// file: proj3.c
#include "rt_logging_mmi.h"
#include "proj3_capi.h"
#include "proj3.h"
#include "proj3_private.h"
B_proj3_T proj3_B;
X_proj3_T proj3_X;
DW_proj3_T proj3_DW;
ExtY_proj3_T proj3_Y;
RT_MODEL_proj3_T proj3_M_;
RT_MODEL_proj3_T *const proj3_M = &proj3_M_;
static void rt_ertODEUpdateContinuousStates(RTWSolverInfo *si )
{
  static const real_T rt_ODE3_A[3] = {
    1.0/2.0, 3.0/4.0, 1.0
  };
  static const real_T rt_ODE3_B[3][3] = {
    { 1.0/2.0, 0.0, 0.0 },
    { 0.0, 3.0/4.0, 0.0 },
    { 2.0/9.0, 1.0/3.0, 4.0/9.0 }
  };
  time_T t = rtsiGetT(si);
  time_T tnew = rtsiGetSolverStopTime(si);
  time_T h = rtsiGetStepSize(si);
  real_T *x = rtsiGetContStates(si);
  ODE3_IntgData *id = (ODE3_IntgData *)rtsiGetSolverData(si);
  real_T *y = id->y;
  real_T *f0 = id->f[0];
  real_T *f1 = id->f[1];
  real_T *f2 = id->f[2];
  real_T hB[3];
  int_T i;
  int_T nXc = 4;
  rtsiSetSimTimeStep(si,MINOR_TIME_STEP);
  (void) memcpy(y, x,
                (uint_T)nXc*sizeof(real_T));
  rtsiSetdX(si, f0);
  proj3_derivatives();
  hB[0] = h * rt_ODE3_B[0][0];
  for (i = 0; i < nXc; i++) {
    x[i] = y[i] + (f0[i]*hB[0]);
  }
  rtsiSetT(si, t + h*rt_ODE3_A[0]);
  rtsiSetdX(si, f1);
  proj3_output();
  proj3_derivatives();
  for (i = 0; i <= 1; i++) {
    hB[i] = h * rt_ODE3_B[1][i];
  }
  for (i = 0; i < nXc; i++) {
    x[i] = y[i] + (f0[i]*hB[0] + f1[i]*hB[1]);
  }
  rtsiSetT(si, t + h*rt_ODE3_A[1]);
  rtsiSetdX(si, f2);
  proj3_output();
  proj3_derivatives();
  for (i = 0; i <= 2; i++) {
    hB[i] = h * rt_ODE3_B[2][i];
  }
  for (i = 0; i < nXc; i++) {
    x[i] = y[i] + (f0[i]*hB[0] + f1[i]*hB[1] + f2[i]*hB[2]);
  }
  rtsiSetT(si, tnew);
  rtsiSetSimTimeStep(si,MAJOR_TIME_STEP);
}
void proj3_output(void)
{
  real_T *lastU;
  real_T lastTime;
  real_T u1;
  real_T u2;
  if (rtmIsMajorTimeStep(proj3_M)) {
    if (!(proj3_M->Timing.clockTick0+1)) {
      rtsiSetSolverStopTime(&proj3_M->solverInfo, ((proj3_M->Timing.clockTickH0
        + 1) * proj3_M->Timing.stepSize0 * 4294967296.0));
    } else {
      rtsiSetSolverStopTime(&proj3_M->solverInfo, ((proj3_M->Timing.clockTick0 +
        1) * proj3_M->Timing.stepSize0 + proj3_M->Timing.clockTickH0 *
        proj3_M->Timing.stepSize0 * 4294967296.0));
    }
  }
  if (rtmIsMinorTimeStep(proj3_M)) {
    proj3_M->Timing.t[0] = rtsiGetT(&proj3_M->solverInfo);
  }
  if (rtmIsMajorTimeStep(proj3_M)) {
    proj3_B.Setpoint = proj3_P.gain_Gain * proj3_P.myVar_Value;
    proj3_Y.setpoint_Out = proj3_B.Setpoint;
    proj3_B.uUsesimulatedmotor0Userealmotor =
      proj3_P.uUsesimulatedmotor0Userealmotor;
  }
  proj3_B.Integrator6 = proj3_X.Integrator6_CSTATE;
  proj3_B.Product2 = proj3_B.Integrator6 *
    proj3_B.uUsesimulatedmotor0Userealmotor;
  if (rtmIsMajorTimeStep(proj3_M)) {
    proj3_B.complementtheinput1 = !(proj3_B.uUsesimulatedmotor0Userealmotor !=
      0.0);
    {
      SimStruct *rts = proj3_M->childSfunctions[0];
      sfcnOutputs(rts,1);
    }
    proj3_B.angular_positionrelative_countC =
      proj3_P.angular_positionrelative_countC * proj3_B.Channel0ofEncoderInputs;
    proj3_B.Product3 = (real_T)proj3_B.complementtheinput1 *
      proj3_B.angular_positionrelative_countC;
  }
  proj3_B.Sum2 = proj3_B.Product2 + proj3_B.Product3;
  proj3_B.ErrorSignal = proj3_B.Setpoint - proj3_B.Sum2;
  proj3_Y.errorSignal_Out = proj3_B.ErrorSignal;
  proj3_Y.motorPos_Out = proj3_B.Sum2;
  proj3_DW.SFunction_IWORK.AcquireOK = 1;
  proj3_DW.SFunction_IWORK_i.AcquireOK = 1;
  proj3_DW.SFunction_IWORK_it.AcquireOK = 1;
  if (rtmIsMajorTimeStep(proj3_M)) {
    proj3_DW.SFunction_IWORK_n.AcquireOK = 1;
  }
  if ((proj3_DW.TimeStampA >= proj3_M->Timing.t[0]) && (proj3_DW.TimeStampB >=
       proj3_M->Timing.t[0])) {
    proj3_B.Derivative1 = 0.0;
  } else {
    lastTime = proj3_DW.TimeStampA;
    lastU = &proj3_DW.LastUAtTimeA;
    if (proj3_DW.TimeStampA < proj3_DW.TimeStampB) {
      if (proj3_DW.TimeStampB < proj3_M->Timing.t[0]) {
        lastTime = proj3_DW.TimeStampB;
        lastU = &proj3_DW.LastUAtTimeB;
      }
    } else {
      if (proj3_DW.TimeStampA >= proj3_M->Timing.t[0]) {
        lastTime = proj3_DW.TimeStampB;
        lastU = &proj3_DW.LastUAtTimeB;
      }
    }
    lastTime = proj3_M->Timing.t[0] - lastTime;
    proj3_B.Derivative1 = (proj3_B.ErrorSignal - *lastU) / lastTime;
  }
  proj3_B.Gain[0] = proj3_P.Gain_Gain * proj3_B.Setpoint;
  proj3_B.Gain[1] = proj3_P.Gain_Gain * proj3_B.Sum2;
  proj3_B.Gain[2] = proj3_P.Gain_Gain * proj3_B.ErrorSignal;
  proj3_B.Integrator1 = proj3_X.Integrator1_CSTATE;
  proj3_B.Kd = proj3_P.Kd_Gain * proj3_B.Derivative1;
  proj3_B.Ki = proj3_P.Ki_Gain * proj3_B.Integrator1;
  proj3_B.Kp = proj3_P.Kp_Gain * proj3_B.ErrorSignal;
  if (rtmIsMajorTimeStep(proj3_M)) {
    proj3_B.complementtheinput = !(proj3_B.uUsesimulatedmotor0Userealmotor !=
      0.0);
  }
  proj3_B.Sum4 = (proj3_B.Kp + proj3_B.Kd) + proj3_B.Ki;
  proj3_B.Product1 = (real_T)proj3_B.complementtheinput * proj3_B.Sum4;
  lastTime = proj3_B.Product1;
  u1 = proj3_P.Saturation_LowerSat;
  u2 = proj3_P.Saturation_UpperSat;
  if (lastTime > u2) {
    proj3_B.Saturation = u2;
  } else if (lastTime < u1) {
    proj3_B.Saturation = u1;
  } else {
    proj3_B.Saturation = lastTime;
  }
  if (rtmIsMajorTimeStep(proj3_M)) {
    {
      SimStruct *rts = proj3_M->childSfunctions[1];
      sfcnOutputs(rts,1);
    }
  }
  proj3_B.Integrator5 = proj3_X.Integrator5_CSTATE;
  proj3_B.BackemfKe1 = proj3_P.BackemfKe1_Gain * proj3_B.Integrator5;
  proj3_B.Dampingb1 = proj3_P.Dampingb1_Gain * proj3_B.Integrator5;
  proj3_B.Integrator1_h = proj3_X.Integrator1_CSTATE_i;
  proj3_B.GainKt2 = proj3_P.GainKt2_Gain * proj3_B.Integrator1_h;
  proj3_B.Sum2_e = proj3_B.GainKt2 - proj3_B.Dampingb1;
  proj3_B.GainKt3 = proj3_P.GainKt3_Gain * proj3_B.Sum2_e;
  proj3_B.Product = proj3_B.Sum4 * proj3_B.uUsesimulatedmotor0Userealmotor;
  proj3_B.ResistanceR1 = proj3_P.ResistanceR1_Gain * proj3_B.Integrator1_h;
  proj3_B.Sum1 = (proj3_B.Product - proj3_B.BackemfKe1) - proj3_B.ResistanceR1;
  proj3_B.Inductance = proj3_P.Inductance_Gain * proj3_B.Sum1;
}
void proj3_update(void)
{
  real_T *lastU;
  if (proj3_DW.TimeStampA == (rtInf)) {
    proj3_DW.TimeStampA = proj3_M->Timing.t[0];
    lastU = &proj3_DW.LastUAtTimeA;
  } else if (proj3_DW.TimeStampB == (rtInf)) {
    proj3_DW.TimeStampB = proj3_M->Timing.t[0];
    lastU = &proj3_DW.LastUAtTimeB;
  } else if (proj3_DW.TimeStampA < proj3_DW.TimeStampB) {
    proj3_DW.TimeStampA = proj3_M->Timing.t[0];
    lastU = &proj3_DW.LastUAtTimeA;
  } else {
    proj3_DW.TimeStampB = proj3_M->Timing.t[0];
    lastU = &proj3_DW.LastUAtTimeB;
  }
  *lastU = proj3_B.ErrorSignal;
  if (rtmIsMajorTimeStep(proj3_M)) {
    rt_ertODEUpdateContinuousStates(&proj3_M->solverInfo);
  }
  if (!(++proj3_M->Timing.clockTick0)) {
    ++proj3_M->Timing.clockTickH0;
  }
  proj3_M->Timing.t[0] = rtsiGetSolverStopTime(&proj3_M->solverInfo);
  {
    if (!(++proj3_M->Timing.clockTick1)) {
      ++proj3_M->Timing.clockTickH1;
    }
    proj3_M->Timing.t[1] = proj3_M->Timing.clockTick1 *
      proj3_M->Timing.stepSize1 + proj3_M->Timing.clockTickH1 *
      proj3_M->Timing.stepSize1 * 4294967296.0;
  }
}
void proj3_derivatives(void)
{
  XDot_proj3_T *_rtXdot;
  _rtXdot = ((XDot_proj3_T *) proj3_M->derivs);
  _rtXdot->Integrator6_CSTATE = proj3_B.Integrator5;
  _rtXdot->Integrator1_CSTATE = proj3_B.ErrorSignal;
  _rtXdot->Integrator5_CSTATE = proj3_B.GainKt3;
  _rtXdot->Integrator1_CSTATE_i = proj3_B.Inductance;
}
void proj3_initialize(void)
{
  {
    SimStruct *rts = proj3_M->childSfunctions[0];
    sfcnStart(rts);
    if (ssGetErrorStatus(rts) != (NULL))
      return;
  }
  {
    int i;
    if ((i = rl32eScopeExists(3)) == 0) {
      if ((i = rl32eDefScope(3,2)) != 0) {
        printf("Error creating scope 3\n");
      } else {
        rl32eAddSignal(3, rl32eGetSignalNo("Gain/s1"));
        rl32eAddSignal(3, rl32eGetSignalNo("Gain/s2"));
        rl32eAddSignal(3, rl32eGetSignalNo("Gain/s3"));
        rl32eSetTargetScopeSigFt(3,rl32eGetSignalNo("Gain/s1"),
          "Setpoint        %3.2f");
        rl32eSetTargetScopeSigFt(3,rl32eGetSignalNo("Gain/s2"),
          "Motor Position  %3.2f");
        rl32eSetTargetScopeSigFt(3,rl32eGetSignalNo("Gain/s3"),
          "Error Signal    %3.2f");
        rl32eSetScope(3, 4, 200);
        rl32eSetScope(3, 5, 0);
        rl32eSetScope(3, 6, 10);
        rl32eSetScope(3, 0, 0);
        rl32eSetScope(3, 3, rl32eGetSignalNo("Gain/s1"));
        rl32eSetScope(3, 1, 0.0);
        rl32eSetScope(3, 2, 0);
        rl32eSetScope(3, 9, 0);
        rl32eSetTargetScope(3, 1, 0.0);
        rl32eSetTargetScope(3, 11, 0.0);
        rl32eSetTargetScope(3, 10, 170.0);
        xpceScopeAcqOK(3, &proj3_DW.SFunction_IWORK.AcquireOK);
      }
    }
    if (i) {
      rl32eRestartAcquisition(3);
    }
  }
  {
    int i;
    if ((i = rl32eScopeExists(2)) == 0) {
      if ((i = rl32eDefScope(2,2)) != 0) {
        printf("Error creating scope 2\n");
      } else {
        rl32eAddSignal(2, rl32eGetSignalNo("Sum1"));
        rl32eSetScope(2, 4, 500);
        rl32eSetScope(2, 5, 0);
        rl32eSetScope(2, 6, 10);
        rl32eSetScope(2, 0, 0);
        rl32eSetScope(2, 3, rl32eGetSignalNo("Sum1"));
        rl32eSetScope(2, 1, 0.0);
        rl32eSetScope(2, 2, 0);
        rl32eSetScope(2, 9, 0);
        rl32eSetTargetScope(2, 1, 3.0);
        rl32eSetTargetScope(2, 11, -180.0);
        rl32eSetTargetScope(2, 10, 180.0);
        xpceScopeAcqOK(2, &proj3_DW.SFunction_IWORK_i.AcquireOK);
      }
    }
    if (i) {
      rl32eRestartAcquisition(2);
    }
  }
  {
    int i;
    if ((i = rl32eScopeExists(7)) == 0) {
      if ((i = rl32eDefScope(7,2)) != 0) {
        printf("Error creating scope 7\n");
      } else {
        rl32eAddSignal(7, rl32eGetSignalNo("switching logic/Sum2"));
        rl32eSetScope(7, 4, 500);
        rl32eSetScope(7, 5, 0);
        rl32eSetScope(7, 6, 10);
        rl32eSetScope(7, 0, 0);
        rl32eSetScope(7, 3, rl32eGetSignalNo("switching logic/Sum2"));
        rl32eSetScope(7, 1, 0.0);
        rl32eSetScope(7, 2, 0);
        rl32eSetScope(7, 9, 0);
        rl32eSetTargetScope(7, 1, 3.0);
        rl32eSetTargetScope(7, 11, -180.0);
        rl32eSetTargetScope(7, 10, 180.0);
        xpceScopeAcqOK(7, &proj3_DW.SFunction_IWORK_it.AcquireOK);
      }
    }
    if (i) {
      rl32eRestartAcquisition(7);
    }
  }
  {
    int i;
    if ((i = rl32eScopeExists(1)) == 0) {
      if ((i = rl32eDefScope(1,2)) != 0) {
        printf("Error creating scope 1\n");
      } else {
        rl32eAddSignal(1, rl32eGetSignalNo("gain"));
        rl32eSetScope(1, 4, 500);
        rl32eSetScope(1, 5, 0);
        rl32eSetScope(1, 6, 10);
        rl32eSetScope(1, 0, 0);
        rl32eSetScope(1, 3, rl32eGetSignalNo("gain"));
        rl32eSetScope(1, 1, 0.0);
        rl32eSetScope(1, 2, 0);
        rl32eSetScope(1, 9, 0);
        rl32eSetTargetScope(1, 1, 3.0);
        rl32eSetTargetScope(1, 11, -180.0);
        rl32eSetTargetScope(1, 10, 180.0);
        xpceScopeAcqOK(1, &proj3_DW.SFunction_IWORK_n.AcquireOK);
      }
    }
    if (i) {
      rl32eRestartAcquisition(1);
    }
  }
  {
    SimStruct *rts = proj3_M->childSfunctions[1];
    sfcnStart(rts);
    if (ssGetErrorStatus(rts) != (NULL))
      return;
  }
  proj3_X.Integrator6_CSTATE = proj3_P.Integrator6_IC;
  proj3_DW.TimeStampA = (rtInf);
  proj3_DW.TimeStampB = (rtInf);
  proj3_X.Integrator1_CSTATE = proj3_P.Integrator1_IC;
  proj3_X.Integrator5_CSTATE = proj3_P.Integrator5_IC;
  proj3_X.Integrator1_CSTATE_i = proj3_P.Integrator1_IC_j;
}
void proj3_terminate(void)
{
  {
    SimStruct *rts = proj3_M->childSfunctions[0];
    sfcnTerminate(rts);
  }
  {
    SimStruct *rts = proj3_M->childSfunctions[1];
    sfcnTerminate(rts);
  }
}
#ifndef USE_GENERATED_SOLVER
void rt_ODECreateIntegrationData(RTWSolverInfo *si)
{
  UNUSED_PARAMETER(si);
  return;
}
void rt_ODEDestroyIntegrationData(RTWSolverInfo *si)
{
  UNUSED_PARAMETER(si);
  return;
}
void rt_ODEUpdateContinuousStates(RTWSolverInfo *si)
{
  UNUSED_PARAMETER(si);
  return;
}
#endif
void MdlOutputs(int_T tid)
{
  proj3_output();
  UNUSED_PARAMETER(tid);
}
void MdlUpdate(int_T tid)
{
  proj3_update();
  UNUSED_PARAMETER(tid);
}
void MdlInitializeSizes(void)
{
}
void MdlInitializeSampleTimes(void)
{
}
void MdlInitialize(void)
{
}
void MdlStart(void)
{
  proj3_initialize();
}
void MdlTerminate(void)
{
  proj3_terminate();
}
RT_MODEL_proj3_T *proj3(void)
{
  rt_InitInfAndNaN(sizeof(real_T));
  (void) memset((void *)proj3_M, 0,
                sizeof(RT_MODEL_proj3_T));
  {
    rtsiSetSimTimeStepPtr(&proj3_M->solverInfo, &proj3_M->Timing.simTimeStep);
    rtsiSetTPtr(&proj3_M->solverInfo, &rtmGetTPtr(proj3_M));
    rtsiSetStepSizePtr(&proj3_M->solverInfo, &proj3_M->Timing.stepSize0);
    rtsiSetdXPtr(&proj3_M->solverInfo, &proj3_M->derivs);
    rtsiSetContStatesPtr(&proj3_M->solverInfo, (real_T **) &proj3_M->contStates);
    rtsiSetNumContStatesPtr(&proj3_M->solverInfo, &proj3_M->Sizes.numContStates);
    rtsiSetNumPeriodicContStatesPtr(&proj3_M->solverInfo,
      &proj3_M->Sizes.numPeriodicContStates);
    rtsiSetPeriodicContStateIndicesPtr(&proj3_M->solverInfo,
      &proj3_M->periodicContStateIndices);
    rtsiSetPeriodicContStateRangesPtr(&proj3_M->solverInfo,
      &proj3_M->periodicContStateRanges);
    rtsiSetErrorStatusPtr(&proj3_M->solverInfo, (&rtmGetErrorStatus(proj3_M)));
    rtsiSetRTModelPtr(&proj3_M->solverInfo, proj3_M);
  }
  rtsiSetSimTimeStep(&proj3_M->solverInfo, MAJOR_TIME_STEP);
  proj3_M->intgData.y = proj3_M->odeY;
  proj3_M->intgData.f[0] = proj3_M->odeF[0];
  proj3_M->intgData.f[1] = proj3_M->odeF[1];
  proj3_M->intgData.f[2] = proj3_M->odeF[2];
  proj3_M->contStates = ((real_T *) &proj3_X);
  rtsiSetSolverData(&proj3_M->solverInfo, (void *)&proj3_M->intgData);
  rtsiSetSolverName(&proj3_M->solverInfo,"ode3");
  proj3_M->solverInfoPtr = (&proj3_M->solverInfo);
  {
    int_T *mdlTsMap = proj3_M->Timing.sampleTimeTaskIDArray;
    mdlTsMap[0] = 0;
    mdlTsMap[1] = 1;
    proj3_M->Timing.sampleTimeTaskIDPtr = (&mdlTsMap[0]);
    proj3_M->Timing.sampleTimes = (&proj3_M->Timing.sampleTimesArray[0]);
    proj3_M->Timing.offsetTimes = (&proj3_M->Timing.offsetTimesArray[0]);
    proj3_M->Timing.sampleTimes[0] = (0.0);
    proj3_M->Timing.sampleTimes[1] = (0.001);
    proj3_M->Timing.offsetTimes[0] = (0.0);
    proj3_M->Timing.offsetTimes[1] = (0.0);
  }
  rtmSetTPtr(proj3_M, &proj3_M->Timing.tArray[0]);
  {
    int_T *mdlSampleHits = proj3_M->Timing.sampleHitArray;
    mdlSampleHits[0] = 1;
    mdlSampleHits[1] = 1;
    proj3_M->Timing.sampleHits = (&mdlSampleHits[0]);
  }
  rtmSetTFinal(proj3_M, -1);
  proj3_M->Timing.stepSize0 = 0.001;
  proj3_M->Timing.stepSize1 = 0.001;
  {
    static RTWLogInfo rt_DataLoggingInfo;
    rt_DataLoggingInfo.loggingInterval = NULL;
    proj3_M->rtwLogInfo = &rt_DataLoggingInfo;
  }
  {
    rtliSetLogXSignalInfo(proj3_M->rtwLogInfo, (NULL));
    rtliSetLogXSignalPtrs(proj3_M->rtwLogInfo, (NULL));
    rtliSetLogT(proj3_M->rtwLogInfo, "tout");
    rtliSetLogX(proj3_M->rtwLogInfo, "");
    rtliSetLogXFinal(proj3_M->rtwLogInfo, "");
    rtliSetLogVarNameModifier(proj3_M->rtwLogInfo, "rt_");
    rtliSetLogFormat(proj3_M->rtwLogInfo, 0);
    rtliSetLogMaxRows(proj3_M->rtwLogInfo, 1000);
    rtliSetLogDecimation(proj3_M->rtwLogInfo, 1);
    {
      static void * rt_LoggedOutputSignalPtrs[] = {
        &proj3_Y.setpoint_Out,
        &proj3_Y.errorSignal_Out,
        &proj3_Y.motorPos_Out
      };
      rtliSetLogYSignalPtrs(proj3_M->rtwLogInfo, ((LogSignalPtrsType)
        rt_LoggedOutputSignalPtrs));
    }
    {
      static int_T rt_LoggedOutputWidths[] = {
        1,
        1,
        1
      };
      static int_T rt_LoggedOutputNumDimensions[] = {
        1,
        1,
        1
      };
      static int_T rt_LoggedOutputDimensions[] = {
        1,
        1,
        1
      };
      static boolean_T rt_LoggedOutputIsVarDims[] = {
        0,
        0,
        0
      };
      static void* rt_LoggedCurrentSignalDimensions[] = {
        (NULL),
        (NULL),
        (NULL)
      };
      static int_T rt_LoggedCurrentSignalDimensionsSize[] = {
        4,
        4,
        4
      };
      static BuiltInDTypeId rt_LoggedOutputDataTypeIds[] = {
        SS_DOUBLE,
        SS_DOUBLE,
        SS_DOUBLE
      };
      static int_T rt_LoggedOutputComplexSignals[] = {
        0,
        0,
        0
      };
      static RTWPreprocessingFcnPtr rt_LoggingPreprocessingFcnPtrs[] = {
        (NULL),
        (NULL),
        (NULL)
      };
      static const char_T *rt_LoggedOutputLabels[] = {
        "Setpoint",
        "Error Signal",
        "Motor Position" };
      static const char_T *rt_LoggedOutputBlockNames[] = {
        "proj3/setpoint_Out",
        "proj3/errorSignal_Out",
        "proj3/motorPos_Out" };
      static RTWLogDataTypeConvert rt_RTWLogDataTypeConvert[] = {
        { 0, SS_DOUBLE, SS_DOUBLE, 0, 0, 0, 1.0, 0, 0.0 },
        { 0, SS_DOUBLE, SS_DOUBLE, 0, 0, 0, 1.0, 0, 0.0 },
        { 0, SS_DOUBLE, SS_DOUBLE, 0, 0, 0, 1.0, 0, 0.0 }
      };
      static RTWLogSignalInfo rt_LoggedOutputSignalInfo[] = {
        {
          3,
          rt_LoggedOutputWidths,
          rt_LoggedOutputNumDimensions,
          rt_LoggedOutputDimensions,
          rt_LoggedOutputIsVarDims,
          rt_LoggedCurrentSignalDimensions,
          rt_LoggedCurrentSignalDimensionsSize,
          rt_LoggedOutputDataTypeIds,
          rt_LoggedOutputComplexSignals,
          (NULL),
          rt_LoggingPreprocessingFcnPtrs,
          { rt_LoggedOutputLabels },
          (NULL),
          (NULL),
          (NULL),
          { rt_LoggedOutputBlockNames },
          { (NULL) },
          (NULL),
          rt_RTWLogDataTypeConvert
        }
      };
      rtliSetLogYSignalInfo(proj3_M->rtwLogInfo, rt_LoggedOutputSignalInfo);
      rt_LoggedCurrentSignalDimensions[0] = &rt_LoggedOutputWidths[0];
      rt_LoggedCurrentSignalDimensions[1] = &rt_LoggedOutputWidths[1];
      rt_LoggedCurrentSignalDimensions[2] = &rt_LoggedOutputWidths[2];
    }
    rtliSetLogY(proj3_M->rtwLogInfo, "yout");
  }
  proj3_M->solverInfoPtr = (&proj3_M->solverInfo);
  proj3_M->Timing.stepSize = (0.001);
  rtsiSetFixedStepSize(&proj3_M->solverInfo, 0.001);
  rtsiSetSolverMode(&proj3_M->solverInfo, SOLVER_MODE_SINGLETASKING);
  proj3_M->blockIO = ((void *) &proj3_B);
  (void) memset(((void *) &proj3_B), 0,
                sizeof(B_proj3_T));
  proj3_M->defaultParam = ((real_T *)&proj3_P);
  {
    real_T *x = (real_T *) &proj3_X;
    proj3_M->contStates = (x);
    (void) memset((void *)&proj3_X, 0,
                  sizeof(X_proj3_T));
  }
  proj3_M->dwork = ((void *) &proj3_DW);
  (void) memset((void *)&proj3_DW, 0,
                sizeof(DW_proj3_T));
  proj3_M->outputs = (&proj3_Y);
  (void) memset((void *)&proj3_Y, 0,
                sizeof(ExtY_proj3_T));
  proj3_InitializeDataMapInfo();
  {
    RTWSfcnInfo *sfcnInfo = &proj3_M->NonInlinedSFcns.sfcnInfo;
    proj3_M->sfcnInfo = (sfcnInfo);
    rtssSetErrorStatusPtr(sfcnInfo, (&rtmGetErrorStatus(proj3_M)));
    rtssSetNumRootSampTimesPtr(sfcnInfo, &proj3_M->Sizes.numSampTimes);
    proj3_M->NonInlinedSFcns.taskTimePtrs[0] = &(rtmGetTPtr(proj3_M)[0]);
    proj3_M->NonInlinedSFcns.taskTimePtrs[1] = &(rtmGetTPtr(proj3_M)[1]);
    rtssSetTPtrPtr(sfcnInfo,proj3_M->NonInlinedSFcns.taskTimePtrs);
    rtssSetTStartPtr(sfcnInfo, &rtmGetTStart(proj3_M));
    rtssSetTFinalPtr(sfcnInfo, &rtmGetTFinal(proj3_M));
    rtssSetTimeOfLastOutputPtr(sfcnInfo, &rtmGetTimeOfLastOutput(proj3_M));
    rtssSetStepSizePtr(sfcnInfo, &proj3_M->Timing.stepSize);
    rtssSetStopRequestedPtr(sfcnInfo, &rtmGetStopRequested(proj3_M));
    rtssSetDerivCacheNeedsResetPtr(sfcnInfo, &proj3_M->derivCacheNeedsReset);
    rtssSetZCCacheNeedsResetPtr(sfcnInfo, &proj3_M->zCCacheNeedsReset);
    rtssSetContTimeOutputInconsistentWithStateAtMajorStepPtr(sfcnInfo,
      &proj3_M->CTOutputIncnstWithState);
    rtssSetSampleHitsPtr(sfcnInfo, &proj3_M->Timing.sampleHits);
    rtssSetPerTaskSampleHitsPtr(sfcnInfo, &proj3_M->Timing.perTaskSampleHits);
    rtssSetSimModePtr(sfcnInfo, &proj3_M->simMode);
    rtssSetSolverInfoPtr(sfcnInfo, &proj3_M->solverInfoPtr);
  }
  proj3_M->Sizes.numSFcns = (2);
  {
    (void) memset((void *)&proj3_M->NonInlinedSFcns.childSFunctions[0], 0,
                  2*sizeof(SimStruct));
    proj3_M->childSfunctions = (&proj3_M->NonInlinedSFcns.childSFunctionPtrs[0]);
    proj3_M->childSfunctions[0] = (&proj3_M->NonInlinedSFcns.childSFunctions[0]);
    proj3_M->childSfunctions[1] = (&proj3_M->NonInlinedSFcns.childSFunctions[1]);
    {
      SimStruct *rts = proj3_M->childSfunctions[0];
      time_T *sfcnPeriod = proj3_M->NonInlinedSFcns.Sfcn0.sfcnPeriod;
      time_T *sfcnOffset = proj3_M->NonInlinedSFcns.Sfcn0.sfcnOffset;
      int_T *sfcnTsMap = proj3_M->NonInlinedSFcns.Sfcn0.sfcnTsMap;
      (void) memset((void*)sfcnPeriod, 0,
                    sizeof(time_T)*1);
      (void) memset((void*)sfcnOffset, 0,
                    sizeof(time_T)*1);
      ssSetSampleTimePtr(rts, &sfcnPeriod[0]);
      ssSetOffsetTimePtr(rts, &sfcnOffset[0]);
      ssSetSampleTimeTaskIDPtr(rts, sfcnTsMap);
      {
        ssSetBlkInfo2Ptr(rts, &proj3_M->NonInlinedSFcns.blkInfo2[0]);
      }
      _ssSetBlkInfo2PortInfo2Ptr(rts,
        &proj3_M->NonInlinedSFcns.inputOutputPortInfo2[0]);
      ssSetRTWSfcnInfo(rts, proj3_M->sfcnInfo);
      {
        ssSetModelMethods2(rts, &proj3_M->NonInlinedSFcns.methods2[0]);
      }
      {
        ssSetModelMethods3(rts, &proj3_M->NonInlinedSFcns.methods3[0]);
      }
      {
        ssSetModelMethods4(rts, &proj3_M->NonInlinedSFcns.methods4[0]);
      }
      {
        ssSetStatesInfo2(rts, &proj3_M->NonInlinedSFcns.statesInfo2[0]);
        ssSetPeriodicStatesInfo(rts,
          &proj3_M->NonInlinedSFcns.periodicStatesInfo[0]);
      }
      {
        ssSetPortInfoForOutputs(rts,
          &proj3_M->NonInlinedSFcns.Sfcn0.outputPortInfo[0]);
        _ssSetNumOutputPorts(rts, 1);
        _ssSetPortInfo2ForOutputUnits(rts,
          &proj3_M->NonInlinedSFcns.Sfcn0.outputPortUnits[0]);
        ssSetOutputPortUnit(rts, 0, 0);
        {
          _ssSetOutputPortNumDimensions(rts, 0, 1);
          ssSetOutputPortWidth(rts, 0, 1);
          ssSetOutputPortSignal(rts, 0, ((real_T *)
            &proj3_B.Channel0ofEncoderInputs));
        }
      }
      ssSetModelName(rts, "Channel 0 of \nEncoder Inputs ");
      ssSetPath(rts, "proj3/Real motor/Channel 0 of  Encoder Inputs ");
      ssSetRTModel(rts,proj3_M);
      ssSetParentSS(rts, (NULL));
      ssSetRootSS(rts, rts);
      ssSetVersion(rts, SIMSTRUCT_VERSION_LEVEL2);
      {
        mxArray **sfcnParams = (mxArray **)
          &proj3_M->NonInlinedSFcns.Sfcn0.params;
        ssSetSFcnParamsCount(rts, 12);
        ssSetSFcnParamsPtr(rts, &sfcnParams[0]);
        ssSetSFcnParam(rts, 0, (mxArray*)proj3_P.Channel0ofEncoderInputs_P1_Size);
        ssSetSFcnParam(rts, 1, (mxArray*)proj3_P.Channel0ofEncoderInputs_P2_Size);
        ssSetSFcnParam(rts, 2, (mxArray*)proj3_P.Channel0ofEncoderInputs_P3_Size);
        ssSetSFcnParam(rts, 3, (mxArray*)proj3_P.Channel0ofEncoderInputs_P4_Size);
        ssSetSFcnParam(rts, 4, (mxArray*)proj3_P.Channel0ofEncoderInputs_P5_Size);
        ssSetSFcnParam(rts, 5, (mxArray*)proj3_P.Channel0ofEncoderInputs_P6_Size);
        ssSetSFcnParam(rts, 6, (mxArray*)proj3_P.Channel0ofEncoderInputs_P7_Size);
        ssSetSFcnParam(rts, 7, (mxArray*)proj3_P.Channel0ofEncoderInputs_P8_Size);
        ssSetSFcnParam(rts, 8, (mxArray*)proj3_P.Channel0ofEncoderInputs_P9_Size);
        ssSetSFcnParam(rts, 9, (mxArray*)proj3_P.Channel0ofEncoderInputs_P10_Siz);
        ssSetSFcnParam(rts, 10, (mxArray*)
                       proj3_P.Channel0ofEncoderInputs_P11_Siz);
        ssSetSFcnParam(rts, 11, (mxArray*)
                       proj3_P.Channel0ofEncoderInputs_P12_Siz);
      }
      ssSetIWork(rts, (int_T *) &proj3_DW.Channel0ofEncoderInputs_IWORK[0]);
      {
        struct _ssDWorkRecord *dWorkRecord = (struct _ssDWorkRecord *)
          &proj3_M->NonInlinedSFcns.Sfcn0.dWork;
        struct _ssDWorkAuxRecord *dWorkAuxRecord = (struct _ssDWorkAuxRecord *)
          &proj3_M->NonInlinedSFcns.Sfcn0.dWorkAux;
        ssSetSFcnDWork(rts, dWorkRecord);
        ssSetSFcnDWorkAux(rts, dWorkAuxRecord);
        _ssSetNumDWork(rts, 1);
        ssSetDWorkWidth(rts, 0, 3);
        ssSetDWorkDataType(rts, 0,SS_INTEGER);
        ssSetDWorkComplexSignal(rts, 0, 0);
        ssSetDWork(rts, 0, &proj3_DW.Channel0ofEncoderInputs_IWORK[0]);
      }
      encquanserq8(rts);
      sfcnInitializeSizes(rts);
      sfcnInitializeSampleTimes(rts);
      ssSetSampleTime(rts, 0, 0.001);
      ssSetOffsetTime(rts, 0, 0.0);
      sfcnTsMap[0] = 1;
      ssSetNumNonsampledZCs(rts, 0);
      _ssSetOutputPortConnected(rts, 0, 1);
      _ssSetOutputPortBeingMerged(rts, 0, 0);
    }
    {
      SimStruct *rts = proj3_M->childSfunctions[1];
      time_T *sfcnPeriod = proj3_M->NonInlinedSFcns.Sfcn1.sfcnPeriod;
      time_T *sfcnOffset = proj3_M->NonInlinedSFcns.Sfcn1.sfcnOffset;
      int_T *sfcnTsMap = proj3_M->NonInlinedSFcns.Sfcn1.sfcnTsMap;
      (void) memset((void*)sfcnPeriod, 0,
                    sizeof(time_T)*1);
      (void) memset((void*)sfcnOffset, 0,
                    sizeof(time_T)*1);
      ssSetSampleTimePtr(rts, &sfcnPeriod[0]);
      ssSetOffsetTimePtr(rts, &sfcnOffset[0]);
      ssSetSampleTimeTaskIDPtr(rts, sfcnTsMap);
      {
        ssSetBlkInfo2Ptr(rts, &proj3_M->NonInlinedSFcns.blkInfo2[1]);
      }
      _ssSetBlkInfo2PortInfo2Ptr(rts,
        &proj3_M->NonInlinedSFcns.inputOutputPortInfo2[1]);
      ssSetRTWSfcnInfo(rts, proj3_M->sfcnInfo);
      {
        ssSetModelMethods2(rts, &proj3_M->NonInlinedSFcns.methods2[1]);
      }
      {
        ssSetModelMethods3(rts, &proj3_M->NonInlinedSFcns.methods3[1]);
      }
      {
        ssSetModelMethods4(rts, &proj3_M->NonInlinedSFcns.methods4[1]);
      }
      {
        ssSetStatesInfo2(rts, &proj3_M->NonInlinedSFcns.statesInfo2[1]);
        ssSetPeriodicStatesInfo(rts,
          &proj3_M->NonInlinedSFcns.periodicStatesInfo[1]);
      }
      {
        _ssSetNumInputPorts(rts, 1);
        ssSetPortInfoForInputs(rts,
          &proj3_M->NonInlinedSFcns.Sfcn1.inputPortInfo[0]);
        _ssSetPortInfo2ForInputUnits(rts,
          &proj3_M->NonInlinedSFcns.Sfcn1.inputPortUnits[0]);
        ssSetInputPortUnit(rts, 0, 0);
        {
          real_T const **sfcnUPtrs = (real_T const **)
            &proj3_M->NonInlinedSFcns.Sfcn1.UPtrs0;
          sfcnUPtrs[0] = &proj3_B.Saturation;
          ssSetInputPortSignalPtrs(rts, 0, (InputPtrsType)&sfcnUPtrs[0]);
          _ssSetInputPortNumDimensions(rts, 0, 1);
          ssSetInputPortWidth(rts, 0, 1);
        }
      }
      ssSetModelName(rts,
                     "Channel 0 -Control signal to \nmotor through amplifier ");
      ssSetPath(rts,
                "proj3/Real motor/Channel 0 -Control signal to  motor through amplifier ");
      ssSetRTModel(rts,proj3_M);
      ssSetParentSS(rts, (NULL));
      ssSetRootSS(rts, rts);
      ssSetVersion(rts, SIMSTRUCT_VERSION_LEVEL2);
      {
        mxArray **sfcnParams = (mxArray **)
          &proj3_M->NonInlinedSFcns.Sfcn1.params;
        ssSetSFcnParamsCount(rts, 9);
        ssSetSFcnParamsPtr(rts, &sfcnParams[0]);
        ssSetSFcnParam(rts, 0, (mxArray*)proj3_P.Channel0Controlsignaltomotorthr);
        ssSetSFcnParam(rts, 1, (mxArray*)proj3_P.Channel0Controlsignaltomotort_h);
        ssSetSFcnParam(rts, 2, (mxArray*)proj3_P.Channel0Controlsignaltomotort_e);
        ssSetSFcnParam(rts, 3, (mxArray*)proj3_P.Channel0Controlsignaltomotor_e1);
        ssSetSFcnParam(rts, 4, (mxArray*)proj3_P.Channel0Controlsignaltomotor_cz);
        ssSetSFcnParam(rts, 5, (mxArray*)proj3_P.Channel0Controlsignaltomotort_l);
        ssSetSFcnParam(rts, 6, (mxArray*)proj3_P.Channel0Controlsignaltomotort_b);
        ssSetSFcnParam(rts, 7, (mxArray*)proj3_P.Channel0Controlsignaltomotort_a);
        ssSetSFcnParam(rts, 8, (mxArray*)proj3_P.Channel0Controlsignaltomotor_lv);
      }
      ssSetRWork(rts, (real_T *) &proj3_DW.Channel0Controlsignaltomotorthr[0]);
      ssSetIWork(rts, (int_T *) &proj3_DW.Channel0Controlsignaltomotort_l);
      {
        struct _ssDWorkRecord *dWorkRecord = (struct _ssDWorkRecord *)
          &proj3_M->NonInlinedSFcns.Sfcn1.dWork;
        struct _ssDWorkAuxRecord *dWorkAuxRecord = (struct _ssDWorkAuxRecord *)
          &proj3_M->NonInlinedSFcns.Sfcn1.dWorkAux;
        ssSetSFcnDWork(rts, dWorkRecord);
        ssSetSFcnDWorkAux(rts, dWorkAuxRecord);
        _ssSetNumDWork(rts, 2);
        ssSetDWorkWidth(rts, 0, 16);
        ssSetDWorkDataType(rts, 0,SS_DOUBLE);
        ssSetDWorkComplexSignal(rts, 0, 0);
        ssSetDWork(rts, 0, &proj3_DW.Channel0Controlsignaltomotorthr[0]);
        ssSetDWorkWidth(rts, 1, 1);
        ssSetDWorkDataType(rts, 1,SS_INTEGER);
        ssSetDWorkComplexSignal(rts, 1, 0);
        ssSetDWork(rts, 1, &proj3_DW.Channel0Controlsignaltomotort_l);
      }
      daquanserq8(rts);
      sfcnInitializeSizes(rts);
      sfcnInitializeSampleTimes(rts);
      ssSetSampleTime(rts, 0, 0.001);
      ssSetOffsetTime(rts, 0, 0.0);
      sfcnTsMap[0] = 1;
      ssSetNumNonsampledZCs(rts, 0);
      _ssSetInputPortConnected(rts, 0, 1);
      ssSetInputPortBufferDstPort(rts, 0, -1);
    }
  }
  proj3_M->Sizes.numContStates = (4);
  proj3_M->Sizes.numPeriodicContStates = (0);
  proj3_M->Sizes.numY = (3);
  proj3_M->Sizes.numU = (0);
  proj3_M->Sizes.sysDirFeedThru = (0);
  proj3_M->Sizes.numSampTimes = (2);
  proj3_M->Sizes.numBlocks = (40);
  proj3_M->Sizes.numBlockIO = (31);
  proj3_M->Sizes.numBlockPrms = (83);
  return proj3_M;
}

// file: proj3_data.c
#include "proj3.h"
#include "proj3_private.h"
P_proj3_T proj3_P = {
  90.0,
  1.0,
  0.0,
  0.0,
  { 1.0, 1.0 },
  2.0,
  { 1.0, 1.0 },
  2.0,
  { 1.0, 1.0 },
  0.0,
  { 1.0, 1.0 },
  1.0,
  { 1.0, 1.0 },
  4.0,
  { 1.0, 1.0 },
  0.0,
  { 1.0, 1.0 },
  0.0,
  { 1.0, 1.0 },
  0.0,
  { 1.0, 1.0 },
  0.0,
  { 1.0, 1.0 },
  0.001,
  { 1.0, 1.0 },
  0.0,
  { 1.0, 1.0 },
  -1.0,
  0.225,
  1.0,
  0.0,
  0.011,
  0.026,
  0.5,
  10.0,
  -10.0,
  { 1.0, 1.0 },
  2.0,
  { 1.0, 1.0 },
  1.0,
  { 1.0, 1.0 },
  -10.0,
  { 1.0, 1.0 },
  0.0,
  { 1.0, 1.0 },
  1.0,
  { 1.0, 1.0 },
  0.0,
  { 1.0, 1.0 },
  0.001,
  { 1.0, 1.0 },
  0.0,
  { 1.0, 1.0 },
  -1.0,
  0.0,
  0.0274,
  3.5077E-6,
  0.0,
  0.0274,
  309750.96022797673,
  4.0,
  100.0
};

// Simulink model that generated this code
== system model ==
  setpoint_Out : Outport  <- 1: gain
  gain : Gain  <- 1: myVar
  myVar : Constant  Value=90
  errorSignal_Out : Outport  <- 1: Sum1
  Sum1 : Sum  Inputs=+-  <- 1: gain, 2: Sum2
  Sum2 : Sum  Inputs=++  <- 1: Product2, 2: Product3
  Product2 : Product  <- 1: Integrator6, 2: Constant#1
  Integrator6 : Integrator  <- 1: Integrator5
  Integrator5 : Integrator  <- 1: GainKt3
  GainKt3 : Gain  Gain=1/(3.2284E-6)  <- 1: Sum#1
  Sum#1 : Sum  Inputs=+-  <- 1: GainKt2, 2: Dampingb1
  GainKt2 : Gain  Gain=0.0274  <- 1: Integrator1
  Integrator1 : Integrator  <- 1: Inductance
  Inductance : Gain  Gain=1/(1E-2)  <- 1: Sum#2
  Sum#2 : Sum  Inputs=+--  <- 1: Product, 2: BackemfKe1, 3: ResistanceR1
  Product : Product  <- 1: Sum4, 2: Constant#1
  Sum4 : Sum  Inputs=+++  <- 1: Kp, 2: Kd, 3: Ki
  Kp : Gain  Gain=.5  <- 1: Sum1
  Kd : Gain  Gain=.011  <- 1: Derivative1
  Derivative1 : Derivative  <- 1: Sum1
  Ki : Gain  Gain=.026  <- 1: Integrator#1
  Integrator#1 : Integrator  <- 1: Sum1
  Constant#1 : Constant  Value=0
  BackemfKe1 : Gain  Gain=0.0274  <- 1: Integrator5
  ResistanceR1 : Gain  Gain=4  <- 1: Integrator1
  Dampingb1 : Gain  Gain=3.5077E-6  <- 1: Integrator5
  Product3 : Product  <- 1: complementtheinput1, 2: Gain#1
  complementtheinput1 : Logic  Operator=NOT  <- 1: Constant#1
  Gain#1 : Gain  Gain=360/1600  <- 1: Channel0ofEncoderInputs
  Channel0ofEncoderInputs : xpcquanserlib/Incremental Encoder/Q4 Enc
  motorPos_Out : Outport  <- 1: Sum2
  Gain : Gain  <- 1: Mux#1
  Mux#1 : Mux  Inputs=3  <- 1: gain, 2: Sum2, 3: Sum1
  Q4DA#1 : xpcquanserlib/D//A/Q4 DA  <- 1: Saturation
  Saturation : Saturate  UpperLimit=10  LowerLimit=-10  <- 1: Product1
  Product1 : Product  <- 1: complementtheinput, 2: Sum4
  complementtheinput : Logic  Operator=NOT  <- 1: Constant#1
